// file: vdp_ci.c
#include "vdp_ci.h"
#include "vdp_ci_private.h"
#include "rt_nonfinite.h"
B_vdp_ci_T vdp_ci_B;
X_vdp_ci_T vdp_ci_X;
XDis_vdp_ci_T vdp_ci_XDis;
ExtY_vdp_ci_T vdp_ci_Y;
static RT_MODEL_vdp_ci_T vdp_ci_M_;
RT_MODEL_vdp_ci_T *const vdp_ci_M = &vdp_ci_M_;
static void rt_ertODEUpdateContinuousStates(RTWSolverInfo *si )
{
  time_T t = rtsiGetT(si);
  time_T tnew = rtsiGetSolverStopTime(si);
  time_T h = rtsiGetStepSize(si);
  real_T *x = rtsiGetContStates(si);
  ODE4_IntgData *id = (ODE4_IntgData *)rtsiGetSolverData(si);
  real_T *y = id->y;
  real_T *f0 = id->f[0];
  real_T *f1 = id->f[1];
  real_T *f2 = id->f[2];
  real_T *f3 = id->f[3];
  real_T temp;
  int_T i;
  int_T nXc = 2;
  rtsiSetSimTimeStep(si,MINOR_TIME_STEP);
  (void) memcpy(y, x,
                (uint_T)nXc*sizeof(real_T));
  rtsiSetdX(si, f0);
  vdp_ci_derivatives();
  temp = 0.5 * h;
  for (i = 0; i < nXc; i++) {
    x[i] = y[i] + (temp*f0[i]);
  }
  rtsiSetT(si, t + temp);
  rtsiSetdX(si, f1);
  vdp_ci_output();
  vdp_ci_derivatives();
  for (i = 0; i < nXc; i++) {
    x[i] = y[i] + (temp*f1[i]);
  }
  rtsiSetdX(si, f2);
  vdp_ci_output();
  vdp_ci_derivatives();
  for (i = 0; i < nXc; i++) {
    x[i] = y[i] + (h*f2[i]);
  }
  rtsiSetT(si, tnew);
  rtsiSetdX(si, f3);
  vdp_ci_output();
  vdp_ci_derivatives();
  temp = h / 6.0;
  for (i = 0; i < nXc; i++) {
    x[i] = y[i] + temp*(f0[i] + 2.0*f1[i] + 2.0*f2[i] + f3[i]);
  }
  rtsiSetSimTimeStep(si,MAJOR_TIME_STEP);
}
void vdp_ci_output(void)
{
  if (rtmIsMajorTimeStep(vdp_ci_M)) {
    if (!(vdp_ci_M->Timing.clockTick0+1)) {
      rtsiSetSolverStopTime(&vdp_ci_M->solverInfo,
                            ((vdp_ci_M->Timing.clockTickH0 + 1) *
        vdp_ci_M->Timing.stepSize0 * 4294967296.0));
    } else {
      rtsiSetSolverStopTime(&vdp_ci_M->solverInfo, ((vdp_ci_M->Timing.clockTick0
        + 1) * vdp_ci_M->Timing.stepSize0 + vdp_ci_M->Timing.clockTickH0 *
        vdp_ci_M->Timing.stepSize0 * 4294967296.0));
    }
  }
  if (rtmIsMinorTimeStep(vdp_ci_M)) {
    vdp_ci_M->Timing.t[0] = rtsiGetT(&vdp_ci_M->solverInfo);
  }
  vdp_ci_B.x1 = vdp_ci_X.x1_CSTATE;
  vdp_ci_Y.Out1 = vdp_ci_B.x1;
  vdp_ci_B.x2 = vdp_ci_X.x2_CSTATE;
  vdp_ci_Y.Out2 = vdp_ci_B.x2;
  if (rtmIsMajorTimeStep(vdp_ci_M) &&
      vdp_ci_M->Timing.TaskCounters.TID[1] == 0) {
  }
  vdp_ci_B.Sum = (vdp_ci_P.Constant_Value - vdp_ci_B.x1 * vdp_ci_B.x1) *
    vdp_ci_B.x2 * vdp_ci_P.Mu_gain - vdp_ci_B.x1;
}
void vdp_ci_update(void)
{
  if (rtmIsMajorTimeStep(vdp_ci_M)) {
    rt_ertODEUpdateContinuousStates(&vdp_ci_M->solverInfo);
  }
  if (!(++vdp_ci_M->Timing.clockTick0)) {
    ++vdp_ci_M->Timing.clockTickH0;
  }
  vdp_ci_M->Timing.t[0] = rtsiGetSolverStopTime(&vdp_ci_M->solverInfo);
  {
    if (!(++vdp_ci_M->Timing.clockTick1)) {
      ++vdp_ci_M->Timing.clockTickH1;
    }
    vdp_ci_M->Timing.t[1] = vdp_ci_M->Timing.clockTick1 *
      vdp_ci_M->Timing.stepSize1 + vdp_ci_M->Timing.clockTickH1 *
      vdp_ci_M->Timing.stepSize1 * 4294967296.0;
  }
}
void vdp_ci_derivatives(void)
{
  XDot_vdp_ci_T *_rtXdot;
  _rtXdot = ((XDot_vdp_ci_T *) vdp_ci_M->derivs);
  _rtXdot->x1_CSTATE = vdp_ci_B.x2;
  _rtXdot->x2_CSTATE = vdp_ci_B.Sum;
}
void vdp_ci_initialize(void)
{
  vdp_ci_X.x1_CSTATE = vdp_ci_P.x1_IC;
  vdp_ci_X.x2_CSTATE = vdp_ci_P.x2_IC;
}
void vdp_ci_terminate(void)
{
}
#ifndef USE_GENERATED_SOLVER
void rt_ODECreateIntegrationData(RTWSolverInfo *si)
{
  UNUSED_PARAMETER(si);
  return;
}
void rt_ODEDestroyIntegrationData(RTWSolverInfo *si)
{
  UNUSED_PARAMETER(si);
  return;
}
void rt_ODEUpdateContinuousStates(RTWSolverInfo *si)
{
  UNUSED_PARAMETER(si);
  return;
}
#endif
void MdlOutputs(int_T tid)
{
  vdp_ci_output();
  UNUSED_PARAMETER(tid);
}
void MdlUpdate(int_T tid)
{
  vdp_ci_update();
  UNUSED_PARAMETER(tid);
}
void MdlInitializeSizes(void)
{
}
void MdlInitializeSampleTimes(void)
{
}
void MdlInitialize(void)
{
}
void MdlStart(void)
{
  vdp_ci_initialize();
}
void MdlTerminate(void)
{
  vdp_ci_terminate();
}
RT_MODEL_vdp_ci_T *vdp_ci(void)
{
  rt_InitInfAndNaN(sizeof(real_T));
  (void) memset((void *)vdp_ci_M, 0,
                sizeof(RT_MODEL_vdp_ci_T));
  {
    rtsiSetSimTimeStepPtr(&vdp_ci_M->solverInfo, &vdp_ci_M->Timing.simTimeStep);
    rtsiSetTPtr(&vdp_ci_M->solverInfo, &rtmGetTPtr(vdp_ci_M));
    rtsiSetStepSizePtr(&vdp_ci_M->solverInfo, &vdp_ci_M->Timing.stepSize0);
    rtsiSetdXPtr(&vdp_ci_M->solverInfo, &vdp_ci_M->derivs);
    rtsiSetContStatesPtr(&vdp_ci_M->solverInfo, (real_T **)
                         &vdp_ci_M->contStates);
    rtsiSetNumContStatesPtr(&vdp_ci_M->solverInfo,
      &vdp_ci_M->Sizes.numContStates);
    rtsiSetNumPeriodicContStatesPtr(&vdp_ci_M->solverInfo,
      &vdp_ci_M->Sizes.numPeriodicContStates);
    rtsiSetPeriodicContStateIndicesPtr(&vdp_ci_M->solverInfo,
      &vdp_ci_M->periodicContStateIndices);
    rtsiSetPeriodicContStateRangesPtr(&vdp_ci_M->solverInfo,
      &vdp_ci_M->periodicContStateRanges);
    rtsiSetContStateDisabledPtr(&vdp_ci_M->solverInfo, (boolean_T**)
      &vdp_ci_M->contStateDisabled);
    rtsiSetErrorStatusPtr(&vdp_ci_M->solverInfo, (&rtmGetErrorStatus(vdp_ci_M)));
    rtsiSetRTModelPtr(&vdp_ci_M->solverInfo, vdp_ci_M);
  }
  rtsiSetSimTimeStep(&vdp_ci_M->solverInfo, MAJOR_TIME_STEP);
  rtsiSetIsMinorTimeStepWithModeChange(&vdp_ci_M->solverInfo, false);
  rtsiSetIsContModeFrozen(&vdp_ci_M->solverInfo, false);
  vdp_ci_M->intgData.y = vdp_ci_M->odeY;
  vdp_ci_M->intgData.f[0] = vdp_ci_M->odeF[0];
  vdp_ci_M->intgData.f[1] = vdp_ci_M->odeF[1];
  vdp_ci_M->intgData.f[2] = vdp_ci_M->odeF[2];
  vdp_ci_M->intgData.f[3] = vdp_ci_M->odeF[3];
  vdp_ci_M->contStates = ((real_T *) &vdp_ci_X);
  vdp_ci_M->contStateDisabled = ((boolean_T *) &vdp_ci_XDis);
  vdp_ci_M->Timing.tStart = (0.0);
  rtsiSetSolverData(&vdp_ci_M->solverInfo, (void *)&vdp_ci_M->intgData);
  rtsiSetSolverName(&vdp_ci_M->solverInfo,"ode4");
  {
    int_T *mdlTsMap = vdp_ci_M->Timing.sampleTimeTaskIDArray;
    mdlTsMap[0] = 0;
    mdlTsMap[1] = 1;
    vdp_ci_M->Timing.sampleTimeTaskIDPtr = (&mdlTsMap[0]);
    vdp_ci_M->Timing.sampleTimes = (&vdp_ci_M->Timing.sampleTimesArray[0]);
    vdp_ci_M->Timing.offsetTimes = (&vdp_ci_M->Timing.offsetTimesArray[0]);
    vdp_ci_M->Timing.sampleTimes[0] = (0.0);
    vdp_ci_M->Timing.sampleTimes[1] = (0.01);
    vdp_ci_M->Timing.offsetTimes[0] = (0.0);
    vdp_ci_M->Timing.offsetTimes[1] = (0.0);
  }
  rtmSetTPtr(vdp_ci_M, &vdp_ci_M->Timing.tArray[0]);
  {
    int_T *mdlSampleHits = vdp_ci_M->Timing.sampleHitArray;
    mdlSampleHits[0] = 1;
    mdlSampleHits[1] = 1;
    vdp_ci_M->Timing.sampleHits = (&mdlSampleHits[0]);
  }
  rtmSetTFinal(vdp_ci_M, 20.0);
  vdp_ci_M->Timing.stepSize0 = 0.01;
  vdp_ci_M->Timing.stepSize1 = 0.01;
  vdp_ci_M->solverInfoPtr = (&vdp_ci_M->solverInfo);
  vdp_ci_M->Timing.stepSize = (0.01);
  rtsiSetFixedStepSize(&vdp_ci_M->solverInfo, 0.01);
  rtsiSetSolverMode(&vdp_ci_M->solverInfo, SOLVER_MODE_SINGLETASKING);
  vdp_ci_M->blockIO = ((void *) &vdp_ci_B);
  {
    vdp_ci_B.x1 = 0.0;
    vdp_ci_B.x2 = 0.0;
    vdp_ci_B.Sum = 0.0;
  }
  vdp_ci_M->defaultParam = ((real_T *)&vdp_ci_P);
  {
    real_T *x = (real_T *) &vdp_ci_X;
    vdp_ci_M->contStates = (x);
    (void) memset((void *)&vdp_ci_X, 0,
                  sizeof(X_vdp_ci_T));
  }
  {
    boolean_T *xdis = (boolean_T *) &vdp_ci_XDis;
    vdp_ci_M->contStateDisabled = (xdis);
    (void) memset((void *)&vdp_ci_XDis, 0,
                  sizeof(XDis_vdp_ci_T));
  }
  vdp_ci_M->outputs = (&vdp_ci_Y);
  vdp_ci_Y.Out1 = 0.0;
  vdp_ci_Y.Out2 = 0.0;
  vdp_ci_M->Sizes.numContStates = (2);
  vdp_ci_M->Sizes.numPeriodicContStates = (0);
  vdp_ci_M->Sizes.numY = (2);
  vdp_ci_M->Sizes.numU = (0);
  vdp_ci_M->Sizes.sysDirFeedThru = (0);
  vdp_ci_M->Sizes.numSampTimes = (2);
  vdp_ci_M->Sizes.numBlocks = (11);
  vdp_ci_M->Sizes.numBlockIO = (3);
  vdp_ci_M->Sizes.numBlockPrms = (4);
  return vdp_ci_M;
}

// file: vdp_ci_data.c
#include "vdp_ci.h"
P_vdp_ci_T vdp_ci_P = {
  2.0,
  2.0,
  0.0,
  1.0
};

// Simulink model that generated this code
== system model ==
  Out1 : Outport  InitialOutput=0  <- 1: x1
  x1 : Integrator  InitialCondition=2  <- 1: x2
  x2 : Integrator  <- 1: Sum
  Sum : Sum  Inputs=-+  <- 1: x1, 2: Mu
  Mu : simulink/Math Operations/Slider Gain  <- 1: Product#1
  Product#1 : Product  <- 1: Sum#1, 2: x2
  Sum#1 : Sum  Inputs=+-  <- 1: Constant, 2: Math#1
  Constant : Constant
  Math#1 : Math  Operator=square  <- 1: x1
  Out2 : Outport  InitialOutput=0  <- 1: x2
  CustomCallbackButton#1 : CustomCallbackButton
